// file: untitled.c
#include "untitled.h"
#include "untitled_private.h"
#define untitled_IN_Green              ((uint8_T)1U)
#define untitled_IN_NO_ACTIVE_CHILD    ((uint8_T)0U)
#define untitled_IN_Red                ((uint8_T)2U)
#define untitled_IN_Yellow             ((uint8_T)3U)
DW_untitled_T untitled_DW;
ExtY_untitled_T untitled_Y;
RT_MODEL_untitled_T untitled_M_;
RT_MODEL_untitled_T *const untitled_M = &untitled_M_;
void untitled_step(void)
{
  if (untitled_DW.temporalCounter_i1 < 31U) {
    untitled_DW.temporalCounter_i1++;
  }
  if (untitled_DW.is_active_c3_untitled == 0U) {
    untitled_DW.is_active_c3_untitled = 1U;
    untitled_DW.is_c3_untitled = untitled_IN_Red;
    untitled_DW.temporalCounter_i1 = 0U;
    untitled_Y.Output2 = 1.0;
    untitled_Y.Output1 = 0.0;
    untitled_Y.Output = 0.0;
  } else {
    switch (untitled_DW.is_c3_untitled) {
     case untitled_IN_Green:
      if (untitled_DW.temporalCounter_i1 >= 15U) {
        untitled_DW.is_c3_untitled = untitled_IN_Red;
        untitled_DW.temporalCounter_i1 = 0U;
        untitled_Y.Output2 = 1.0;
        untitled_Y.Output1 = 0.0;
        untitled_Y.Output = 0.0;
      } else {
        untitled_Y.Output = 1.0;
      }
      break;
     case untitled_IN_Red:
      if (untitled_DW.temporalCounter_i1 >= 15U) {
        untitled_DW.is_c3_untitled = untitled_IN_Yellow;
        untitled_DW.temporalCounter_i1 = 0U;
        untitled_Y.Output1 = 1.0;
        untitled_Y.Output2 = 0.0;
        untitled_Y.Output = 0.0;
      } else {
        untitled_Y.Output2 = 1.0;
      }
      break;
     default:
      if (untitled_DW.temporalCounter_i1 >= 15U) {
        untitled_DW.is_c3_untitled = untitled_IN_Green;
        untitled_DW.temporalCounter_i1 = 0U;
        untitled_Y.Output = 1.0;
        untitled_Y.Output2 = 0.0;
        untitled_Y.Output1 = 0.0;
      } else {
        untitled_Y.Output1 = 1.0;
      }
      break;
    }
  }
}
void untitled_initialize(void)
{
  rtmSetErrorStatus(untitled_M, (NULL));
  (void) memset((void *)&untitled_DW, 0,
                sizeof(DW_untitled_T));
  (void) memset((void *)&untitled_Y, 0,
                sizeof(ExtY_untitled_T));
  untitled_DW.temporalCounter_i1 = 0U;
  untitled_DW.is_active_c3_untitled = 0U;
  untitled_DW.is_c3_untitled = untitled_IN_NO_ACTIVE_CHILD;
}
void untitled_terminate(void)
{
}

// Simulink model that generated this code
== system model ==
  Output : Outport  <- 1: Stateflowchart#1
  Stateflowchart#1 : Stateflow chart
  Output1 : Outport  <- 1: Stateflowchart#1/3
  Output2 : Outport  <- 1: Stateflowchart#1/2
== stateflow chart Stateflowchart#1 ==
  state Yellow
    en:
    Yellow_led=1;
    Red_led=0;
    Green_led=0;
    du:
    Yellow_led=1;
    ex:
    Yellow_led=0;
  state Red
    en:
    Red_led=1;
    Yellow_led=0;
    Green_led=0;
    du:
    Red_led=1;
    ex:
    Red_led=0;
  state Green
    en:
    Green_led=1;
    Red_led=0;
    Yellow_led=0;
    du:
    Green_led=1;
    ex:
    Green_led=0;
  (default) -> Red
  Red -> Yellow : [after(3,sec)]
  Green -> Red : [after(3,sec)]
  Yellow -> Green : [after(3,sec)]
  data: Green_led output double; Red_led output double; Yellow_led output double
